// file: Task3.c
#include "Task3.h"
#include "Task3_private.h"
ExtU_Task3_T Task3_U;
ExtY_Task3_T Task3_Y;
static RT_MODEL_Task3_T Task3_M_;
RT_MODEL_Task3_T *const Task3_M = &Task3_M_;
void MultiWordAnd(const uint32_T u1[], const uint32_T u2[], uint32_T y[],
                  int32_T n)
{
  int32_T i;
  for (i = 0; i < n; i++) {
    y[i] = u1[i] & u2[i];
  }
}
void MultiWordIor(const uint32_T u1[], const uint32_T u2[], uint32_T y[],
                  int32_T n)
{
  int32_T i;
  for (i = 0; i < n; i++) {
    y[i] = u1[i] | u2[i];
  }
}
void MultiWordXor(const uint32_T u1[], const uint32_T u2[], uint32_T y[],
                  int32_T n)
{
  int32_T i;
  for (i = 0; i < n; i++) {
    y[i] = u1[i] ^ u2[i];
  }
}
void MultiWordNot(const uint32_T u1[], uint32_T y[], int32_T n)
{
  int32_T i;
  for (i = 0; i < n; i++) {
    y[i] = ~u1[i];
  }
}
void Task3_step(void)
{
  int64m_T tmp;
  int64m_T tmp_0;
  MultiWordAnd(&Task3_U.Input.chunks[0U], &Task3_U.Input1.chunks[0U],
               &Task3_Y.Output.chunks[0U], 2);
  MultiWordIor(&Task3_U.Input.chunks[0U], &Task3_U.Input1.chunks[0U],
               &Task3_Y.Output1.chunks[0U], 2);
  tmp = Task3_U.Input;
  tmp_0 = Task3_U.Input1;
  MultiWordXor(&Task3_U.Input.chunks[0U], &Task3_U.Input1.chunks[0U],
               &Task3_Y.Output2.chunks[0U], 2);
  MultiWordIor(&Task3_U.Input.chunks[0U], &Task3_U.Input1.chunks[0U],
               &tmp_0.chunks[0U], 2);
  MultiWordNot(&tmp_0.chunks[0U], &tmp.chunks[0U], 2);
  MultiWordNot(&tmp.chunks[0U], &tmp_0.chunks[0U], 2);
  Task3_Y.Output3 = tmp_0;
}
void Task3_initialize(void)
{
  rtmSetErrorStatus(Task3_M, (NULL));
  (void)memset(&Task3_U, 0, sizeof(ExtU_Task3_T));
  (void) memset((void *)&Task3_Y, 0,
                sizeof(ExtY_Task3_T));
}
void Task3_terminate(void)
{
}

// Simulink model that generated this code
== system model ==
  Input : Inport
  Input1 : Inport
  Output : Outport  <- 1: BitwiseOperator#1
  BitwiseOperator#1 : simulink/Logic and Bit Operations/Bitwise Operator  logicop=AND  BitMask=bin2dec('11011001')  <- 1: Input, 2: Input1
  Output1 : Outport  <- 1: BitwiseOperator#2
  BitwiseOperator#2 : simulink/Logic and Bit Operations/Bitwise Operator  logicop=OR  BitMask=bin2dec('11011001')  <- 1: Input, 2: Input1
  Output2 : Outport  <- 1: BitwiseOperator#3
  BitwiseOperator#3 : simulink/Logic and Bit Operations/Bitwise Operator  logicop=XOR  BitMask=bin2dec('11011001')  <- 1: Input, 2: Input1
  Output3 : Outport  <- 1: BitwiseOperator#4
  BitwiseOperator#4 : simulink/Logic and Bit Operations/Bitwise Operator  logicop=NOT  BitMask=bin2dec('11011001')  <- 1: BitwiseOperator#5
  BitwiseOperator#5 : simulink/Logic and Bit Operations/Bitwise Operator  logicop=NOR  BitMask=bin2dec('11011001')  <- 1: Input, 2: Input1
